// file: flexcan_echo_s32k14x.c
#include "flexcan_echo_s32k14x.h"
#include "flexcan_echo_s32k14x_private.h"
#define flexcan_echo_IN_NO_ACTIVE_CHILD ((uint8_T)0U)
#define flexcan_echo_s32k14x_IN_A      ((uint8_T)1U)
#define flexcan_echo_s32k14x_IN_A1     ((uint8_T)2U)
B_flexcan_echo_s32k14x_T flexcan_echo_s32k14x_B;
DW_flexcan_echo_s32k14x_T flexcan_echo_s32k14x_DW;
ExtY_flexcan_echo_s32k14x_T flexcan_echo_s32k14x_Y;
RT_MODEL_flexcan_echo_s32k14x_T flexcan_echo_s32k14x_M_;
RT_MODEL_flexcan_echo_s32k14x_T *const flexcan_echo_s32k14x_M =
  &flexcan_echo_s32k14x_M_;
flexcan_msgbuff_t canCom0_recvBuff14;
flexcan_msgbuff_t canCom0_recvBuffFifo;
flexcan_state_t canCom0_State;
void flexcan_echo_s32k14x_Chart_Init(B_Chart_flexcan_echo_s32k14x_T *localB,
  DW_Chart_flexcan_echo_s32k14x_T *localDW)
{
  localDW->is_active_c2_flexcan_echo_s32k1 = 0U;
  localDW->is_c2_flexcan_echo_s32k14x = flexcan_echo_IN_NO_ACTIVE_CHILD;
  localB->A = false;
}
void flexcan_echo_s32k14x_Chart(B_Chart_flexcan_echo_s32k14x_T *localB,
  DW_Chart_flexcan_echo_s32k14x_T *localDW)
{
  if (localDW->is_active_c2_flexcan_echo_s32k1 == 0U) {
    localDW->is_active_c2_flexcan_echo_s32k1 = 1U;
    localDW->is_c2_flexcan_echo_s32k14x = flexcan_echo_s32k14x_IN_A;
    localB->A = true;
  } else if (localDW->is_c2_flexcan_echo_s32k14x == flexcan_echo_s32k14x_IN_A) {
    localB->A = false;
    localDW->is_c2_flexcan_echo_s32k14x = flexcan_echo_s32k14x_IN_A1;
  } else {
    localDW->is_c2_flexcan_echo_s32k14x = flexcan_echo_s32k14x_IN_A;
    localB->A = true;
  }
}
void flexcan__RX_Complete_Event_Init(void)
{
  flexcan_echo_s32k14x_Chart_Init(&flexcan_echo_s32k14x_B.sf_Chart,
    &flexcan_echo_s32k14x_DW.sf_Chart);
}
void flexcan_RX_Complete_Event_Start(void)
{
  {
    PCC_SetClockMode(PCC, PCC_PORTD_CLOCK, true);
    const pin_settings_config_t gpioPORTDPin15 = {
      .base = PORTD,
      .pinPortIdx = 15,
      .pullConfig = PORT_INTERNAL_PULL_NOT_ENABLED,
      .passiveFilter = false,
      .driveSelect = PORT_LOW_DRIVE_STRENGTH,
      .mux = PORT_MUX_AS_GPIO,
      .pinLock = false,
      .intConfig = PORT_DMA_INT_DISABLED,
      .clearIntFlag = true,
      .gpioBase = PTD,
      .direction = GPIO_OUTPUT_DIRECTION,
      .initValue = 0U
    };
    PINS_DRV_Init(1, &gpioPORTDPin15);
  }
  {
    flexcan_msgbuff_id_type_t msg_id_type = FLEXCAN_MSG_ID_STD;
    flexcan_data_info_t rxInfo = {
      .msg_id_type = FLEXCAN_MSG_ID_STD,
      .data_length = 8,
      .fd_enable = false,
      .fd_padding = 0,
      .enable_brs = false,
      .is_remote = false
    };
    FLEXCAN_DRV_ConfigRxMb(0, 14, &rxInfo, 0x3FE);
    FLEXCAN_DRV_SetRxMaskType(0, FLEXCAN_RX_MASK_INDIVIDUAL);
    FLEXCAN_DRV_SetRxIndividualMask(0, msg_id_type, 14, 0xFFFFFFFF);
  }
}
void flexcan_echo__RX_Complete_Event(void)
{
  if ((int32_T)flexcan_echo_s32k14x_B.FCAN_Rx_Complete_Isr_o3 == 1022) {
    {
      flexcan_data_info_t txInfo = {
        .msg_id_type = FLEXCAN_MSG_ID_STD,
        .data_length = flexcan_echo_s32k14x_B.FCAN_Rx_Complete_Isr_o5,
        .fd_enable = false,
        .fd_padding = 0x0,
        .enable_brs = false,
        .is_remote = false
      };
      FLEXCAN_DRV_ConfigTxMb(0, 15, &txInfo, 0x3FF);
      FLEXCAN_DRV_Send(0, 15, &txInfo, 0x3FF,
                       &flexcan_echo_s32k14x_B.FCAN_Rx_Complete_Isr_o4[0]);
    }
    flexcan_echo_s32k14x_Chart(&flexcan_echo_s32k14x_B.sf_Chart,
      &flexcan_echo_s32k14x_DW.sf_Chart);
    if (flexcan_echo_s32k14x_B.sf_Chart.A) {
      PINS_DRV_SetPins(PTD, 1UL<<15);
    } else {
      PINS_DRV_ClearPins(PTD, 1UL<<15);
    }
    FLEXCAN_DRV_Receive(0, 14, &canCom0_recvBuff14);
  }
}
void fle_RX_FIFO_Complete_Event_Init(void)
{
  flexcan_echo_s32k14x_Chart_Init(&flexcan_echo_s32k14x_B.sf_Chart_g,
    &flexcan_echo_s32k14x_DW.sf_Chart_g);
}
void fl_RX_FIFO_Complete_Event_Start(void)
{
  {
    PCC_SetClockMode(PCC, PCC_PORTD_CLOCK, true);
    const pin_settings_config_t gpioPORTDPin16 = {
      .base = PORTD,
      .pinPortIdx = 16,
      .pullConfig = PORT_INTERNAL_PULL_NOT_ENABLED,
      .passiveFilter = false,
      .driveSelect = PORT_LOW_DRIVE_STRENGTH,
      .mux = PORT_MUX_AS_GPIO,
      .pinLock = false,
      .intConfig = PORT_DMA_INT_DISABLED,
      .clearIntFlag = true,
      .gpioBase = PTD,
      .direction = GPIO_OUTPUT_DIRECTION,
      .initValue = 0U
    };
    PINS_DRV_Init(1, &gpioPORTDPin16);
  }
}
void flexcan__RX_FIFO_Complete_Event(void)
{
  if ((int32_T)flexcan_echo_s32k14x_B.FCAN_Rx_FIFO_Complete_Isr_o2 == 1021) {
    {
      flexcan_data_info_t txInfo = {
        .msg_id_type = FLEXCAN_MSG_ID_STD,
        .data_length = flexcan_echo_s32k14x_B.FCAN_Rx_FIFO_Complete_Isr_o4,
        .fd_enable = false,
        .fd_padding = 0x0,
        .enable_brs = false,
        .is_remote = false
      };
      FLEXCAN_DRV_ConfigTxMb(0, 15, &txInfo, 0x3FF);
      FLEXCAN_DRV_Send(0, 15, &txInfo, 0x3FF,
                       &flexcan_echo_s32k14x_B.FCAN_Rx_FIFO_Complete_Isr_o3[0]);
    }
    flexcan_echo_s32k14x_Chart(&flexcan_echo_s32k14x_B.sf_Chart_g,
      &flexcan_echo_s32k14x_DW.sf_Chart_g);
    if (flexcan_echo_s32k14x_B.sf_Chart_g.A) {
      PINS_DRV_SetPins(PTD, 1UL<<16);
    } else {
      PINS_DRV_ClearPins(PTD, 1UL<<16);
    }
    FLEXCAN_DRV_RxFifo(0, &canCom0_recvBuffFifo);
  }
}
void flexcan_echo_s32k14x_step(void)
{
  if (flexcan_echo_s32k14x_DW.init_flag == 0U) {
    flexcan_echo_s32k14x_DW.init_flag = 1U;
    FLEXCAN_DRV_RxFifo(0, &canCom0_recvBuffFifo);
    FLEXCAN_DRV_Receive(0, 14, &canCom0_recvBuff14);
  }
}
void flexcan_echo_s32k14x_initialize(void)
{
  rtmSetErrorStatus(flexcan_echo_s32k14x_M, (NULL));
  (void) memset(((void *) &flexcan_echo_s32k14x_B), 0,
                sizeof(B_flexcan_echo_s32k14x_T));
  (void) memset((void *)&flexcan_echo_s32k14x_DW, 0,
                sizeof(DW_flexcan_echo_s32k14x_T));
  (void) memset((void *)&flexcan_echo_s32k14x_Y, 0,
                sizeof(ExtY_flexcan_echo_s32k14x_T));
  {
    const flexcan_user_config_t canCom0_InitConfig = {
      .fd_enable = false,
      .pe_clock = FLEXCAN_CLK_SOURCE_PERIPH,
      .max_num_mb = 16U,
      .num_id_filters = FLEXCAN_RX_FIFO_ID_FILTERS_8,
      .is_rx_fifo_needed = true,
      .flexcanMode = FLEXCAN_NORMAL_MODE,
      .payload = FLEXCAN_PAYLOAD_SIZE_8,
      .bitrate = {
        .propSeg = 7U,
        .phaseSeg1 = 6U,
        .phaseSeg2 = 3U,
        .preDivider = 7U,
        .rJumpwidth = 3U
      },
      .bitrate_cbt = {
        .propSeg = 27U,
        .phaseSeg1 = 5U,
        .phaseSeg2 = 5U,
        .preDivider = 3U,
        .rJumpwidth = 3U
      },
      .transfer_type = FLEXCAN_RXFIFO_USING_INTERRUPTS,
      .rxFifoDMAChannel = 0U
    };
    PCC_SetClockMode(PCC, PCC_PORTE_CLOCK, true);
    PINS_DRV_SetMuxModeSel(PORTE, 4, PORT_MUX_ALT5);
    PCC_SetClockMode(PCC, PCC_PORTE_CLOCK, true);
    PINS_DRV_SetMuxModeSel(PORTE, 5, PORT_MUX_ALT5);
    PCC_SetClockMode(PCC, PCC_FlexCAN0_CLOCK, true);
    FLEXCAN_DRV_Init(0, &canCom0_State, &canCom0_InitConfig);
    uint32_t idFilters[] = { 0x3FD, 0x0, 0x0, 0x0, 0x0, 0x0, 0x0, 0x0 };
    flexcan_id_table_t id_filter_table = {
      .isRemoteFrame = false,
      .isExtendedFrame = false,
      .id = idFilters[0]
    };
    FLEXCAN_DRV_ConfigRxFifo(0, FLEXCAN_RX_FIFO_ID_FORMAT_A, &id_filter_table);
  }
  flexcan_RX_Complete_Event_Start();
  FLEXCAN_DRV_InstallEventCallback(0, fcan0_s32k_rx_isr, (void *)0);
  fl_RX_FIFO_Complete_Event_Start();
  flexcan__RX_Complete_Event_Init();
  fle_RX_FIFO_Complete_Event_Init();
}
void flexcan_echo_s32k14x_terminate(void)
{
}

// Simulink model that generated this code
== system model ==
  Outport#1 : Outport  <- 1: FCAN_Rx_Complete_Isr/2
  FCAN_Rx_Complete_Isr : mbd_s32k1xx_ec_toolbox/Communication Blocks/CAN Blocks/FCAN_Isr
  Outport#2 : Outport  <- 1: FCAN_Rx_Complete_Isr/6
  Outport#3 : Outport  <- 1: FCAN_Rx_FIFO_Complete_Isr/5
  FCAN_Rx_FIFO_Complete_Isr : mbd_s32k1xx_ec_toolbox/Communication Blocks/CAN Blocks/FCAN_Isr
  RX_Complete_Event : Subsystem  <- 1: FCAN_Rx_Complete_Isr/3, 2: FCAN_Rx_Complete_Isr/4, 3: FCAN_Rx_Complete_Isr/5, Trigger: FCAN_Rx_Complete_Isr
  RX_FIFO_Complete_Event : Subsystem  <- 1: FCAN_Rx_FIFO_Complete_Isr/2, 2: FCAN_Rx_FIFO_Complete_Isr/3, 3: FCAN_Rx_FIFO_Complete_Isr/4, Trigger: FCAN_Rx_FIFO_Complete_Isr
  Subsystem#1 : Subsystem  <- Action: If#1
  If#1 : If  IfExpression=u1 == 0  <- 1: DataStoreRead#1
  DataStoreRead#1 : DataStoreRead  DataStoreName=init_flag
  FCAN_Config#1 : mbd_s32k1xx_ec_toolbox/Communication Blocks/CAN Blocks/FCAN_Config
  DataStoreMemory#1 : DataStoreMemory  DataStoreName=init_flag
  MBD_S32K1xx_Config_Information#1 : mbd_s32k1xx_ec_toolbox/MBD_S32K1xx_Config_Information
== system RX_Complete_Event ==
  ID : Inport
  Inport#1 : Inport
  Inport#2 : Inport
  TriggerPort#1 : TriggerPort  TriggerType=function-call
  Subsystem#2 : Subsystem  <- 1: Inport#1, 2: Inport#2, Action: SwitchCase#1
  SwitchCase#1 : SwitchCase  CaseConditions={hex2dec('3FE')}  <- 1: ID
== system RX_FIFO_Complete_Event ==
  Inport#3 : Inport
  Inport#4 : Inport
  Inport#5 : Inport
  TriggerPort#2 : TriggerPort  TriggerType=function-call
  Subsystem#3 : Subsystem  <- 1: Inport#4, 2: Inport#5, Action: SwitchCase#2
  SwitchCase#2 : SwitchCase  CaseConditions={hex2dec('3FD')}  <- 1: Inport#3
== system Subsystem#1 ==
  ActionPort#1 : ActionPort
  FCAN_Receive#1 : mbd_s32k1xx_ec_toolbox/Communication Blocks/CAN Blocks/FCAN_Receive
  FCAN_Receive#2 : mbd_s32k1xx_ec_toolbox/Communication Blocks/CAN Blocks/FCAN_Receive
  DataStoreWrite#1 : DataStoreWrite  DataStoreName=init_flag  <- 1: Constant#1
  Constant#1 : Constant
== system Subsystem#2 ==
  Inport#6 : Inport
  Inport#7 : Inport
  ActionPort#2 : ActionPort
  Digital_Output#1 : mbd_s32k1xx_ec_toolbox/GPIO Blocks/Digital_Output  <- 1: Chart
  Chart : Stateflow chart
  FCAN_Receive#3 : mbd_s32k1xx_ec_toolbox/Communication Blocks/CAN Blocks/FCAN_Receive
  FCAN_Send#1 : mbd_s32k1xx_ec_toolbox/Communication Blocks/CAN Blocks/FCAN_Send  <- 1: Inport#6, 2: Inport#7
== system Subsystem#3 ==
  Inport#8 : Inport
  Inport#9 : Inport
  ActionPort#3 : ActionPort
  Digital_Output#2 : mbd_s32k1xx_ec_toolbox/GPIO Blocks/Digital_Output  <- 1: Stateflowchart#1
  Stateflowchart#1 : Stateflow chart
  FCAN_Send#2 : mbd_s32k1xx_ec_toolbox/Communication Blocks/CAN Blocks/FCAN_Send  <- 1: Inport#8, 2: Inport#9
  FCAN_Receive#4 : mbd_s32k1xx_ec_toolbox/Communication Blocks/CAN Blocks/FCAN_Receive

